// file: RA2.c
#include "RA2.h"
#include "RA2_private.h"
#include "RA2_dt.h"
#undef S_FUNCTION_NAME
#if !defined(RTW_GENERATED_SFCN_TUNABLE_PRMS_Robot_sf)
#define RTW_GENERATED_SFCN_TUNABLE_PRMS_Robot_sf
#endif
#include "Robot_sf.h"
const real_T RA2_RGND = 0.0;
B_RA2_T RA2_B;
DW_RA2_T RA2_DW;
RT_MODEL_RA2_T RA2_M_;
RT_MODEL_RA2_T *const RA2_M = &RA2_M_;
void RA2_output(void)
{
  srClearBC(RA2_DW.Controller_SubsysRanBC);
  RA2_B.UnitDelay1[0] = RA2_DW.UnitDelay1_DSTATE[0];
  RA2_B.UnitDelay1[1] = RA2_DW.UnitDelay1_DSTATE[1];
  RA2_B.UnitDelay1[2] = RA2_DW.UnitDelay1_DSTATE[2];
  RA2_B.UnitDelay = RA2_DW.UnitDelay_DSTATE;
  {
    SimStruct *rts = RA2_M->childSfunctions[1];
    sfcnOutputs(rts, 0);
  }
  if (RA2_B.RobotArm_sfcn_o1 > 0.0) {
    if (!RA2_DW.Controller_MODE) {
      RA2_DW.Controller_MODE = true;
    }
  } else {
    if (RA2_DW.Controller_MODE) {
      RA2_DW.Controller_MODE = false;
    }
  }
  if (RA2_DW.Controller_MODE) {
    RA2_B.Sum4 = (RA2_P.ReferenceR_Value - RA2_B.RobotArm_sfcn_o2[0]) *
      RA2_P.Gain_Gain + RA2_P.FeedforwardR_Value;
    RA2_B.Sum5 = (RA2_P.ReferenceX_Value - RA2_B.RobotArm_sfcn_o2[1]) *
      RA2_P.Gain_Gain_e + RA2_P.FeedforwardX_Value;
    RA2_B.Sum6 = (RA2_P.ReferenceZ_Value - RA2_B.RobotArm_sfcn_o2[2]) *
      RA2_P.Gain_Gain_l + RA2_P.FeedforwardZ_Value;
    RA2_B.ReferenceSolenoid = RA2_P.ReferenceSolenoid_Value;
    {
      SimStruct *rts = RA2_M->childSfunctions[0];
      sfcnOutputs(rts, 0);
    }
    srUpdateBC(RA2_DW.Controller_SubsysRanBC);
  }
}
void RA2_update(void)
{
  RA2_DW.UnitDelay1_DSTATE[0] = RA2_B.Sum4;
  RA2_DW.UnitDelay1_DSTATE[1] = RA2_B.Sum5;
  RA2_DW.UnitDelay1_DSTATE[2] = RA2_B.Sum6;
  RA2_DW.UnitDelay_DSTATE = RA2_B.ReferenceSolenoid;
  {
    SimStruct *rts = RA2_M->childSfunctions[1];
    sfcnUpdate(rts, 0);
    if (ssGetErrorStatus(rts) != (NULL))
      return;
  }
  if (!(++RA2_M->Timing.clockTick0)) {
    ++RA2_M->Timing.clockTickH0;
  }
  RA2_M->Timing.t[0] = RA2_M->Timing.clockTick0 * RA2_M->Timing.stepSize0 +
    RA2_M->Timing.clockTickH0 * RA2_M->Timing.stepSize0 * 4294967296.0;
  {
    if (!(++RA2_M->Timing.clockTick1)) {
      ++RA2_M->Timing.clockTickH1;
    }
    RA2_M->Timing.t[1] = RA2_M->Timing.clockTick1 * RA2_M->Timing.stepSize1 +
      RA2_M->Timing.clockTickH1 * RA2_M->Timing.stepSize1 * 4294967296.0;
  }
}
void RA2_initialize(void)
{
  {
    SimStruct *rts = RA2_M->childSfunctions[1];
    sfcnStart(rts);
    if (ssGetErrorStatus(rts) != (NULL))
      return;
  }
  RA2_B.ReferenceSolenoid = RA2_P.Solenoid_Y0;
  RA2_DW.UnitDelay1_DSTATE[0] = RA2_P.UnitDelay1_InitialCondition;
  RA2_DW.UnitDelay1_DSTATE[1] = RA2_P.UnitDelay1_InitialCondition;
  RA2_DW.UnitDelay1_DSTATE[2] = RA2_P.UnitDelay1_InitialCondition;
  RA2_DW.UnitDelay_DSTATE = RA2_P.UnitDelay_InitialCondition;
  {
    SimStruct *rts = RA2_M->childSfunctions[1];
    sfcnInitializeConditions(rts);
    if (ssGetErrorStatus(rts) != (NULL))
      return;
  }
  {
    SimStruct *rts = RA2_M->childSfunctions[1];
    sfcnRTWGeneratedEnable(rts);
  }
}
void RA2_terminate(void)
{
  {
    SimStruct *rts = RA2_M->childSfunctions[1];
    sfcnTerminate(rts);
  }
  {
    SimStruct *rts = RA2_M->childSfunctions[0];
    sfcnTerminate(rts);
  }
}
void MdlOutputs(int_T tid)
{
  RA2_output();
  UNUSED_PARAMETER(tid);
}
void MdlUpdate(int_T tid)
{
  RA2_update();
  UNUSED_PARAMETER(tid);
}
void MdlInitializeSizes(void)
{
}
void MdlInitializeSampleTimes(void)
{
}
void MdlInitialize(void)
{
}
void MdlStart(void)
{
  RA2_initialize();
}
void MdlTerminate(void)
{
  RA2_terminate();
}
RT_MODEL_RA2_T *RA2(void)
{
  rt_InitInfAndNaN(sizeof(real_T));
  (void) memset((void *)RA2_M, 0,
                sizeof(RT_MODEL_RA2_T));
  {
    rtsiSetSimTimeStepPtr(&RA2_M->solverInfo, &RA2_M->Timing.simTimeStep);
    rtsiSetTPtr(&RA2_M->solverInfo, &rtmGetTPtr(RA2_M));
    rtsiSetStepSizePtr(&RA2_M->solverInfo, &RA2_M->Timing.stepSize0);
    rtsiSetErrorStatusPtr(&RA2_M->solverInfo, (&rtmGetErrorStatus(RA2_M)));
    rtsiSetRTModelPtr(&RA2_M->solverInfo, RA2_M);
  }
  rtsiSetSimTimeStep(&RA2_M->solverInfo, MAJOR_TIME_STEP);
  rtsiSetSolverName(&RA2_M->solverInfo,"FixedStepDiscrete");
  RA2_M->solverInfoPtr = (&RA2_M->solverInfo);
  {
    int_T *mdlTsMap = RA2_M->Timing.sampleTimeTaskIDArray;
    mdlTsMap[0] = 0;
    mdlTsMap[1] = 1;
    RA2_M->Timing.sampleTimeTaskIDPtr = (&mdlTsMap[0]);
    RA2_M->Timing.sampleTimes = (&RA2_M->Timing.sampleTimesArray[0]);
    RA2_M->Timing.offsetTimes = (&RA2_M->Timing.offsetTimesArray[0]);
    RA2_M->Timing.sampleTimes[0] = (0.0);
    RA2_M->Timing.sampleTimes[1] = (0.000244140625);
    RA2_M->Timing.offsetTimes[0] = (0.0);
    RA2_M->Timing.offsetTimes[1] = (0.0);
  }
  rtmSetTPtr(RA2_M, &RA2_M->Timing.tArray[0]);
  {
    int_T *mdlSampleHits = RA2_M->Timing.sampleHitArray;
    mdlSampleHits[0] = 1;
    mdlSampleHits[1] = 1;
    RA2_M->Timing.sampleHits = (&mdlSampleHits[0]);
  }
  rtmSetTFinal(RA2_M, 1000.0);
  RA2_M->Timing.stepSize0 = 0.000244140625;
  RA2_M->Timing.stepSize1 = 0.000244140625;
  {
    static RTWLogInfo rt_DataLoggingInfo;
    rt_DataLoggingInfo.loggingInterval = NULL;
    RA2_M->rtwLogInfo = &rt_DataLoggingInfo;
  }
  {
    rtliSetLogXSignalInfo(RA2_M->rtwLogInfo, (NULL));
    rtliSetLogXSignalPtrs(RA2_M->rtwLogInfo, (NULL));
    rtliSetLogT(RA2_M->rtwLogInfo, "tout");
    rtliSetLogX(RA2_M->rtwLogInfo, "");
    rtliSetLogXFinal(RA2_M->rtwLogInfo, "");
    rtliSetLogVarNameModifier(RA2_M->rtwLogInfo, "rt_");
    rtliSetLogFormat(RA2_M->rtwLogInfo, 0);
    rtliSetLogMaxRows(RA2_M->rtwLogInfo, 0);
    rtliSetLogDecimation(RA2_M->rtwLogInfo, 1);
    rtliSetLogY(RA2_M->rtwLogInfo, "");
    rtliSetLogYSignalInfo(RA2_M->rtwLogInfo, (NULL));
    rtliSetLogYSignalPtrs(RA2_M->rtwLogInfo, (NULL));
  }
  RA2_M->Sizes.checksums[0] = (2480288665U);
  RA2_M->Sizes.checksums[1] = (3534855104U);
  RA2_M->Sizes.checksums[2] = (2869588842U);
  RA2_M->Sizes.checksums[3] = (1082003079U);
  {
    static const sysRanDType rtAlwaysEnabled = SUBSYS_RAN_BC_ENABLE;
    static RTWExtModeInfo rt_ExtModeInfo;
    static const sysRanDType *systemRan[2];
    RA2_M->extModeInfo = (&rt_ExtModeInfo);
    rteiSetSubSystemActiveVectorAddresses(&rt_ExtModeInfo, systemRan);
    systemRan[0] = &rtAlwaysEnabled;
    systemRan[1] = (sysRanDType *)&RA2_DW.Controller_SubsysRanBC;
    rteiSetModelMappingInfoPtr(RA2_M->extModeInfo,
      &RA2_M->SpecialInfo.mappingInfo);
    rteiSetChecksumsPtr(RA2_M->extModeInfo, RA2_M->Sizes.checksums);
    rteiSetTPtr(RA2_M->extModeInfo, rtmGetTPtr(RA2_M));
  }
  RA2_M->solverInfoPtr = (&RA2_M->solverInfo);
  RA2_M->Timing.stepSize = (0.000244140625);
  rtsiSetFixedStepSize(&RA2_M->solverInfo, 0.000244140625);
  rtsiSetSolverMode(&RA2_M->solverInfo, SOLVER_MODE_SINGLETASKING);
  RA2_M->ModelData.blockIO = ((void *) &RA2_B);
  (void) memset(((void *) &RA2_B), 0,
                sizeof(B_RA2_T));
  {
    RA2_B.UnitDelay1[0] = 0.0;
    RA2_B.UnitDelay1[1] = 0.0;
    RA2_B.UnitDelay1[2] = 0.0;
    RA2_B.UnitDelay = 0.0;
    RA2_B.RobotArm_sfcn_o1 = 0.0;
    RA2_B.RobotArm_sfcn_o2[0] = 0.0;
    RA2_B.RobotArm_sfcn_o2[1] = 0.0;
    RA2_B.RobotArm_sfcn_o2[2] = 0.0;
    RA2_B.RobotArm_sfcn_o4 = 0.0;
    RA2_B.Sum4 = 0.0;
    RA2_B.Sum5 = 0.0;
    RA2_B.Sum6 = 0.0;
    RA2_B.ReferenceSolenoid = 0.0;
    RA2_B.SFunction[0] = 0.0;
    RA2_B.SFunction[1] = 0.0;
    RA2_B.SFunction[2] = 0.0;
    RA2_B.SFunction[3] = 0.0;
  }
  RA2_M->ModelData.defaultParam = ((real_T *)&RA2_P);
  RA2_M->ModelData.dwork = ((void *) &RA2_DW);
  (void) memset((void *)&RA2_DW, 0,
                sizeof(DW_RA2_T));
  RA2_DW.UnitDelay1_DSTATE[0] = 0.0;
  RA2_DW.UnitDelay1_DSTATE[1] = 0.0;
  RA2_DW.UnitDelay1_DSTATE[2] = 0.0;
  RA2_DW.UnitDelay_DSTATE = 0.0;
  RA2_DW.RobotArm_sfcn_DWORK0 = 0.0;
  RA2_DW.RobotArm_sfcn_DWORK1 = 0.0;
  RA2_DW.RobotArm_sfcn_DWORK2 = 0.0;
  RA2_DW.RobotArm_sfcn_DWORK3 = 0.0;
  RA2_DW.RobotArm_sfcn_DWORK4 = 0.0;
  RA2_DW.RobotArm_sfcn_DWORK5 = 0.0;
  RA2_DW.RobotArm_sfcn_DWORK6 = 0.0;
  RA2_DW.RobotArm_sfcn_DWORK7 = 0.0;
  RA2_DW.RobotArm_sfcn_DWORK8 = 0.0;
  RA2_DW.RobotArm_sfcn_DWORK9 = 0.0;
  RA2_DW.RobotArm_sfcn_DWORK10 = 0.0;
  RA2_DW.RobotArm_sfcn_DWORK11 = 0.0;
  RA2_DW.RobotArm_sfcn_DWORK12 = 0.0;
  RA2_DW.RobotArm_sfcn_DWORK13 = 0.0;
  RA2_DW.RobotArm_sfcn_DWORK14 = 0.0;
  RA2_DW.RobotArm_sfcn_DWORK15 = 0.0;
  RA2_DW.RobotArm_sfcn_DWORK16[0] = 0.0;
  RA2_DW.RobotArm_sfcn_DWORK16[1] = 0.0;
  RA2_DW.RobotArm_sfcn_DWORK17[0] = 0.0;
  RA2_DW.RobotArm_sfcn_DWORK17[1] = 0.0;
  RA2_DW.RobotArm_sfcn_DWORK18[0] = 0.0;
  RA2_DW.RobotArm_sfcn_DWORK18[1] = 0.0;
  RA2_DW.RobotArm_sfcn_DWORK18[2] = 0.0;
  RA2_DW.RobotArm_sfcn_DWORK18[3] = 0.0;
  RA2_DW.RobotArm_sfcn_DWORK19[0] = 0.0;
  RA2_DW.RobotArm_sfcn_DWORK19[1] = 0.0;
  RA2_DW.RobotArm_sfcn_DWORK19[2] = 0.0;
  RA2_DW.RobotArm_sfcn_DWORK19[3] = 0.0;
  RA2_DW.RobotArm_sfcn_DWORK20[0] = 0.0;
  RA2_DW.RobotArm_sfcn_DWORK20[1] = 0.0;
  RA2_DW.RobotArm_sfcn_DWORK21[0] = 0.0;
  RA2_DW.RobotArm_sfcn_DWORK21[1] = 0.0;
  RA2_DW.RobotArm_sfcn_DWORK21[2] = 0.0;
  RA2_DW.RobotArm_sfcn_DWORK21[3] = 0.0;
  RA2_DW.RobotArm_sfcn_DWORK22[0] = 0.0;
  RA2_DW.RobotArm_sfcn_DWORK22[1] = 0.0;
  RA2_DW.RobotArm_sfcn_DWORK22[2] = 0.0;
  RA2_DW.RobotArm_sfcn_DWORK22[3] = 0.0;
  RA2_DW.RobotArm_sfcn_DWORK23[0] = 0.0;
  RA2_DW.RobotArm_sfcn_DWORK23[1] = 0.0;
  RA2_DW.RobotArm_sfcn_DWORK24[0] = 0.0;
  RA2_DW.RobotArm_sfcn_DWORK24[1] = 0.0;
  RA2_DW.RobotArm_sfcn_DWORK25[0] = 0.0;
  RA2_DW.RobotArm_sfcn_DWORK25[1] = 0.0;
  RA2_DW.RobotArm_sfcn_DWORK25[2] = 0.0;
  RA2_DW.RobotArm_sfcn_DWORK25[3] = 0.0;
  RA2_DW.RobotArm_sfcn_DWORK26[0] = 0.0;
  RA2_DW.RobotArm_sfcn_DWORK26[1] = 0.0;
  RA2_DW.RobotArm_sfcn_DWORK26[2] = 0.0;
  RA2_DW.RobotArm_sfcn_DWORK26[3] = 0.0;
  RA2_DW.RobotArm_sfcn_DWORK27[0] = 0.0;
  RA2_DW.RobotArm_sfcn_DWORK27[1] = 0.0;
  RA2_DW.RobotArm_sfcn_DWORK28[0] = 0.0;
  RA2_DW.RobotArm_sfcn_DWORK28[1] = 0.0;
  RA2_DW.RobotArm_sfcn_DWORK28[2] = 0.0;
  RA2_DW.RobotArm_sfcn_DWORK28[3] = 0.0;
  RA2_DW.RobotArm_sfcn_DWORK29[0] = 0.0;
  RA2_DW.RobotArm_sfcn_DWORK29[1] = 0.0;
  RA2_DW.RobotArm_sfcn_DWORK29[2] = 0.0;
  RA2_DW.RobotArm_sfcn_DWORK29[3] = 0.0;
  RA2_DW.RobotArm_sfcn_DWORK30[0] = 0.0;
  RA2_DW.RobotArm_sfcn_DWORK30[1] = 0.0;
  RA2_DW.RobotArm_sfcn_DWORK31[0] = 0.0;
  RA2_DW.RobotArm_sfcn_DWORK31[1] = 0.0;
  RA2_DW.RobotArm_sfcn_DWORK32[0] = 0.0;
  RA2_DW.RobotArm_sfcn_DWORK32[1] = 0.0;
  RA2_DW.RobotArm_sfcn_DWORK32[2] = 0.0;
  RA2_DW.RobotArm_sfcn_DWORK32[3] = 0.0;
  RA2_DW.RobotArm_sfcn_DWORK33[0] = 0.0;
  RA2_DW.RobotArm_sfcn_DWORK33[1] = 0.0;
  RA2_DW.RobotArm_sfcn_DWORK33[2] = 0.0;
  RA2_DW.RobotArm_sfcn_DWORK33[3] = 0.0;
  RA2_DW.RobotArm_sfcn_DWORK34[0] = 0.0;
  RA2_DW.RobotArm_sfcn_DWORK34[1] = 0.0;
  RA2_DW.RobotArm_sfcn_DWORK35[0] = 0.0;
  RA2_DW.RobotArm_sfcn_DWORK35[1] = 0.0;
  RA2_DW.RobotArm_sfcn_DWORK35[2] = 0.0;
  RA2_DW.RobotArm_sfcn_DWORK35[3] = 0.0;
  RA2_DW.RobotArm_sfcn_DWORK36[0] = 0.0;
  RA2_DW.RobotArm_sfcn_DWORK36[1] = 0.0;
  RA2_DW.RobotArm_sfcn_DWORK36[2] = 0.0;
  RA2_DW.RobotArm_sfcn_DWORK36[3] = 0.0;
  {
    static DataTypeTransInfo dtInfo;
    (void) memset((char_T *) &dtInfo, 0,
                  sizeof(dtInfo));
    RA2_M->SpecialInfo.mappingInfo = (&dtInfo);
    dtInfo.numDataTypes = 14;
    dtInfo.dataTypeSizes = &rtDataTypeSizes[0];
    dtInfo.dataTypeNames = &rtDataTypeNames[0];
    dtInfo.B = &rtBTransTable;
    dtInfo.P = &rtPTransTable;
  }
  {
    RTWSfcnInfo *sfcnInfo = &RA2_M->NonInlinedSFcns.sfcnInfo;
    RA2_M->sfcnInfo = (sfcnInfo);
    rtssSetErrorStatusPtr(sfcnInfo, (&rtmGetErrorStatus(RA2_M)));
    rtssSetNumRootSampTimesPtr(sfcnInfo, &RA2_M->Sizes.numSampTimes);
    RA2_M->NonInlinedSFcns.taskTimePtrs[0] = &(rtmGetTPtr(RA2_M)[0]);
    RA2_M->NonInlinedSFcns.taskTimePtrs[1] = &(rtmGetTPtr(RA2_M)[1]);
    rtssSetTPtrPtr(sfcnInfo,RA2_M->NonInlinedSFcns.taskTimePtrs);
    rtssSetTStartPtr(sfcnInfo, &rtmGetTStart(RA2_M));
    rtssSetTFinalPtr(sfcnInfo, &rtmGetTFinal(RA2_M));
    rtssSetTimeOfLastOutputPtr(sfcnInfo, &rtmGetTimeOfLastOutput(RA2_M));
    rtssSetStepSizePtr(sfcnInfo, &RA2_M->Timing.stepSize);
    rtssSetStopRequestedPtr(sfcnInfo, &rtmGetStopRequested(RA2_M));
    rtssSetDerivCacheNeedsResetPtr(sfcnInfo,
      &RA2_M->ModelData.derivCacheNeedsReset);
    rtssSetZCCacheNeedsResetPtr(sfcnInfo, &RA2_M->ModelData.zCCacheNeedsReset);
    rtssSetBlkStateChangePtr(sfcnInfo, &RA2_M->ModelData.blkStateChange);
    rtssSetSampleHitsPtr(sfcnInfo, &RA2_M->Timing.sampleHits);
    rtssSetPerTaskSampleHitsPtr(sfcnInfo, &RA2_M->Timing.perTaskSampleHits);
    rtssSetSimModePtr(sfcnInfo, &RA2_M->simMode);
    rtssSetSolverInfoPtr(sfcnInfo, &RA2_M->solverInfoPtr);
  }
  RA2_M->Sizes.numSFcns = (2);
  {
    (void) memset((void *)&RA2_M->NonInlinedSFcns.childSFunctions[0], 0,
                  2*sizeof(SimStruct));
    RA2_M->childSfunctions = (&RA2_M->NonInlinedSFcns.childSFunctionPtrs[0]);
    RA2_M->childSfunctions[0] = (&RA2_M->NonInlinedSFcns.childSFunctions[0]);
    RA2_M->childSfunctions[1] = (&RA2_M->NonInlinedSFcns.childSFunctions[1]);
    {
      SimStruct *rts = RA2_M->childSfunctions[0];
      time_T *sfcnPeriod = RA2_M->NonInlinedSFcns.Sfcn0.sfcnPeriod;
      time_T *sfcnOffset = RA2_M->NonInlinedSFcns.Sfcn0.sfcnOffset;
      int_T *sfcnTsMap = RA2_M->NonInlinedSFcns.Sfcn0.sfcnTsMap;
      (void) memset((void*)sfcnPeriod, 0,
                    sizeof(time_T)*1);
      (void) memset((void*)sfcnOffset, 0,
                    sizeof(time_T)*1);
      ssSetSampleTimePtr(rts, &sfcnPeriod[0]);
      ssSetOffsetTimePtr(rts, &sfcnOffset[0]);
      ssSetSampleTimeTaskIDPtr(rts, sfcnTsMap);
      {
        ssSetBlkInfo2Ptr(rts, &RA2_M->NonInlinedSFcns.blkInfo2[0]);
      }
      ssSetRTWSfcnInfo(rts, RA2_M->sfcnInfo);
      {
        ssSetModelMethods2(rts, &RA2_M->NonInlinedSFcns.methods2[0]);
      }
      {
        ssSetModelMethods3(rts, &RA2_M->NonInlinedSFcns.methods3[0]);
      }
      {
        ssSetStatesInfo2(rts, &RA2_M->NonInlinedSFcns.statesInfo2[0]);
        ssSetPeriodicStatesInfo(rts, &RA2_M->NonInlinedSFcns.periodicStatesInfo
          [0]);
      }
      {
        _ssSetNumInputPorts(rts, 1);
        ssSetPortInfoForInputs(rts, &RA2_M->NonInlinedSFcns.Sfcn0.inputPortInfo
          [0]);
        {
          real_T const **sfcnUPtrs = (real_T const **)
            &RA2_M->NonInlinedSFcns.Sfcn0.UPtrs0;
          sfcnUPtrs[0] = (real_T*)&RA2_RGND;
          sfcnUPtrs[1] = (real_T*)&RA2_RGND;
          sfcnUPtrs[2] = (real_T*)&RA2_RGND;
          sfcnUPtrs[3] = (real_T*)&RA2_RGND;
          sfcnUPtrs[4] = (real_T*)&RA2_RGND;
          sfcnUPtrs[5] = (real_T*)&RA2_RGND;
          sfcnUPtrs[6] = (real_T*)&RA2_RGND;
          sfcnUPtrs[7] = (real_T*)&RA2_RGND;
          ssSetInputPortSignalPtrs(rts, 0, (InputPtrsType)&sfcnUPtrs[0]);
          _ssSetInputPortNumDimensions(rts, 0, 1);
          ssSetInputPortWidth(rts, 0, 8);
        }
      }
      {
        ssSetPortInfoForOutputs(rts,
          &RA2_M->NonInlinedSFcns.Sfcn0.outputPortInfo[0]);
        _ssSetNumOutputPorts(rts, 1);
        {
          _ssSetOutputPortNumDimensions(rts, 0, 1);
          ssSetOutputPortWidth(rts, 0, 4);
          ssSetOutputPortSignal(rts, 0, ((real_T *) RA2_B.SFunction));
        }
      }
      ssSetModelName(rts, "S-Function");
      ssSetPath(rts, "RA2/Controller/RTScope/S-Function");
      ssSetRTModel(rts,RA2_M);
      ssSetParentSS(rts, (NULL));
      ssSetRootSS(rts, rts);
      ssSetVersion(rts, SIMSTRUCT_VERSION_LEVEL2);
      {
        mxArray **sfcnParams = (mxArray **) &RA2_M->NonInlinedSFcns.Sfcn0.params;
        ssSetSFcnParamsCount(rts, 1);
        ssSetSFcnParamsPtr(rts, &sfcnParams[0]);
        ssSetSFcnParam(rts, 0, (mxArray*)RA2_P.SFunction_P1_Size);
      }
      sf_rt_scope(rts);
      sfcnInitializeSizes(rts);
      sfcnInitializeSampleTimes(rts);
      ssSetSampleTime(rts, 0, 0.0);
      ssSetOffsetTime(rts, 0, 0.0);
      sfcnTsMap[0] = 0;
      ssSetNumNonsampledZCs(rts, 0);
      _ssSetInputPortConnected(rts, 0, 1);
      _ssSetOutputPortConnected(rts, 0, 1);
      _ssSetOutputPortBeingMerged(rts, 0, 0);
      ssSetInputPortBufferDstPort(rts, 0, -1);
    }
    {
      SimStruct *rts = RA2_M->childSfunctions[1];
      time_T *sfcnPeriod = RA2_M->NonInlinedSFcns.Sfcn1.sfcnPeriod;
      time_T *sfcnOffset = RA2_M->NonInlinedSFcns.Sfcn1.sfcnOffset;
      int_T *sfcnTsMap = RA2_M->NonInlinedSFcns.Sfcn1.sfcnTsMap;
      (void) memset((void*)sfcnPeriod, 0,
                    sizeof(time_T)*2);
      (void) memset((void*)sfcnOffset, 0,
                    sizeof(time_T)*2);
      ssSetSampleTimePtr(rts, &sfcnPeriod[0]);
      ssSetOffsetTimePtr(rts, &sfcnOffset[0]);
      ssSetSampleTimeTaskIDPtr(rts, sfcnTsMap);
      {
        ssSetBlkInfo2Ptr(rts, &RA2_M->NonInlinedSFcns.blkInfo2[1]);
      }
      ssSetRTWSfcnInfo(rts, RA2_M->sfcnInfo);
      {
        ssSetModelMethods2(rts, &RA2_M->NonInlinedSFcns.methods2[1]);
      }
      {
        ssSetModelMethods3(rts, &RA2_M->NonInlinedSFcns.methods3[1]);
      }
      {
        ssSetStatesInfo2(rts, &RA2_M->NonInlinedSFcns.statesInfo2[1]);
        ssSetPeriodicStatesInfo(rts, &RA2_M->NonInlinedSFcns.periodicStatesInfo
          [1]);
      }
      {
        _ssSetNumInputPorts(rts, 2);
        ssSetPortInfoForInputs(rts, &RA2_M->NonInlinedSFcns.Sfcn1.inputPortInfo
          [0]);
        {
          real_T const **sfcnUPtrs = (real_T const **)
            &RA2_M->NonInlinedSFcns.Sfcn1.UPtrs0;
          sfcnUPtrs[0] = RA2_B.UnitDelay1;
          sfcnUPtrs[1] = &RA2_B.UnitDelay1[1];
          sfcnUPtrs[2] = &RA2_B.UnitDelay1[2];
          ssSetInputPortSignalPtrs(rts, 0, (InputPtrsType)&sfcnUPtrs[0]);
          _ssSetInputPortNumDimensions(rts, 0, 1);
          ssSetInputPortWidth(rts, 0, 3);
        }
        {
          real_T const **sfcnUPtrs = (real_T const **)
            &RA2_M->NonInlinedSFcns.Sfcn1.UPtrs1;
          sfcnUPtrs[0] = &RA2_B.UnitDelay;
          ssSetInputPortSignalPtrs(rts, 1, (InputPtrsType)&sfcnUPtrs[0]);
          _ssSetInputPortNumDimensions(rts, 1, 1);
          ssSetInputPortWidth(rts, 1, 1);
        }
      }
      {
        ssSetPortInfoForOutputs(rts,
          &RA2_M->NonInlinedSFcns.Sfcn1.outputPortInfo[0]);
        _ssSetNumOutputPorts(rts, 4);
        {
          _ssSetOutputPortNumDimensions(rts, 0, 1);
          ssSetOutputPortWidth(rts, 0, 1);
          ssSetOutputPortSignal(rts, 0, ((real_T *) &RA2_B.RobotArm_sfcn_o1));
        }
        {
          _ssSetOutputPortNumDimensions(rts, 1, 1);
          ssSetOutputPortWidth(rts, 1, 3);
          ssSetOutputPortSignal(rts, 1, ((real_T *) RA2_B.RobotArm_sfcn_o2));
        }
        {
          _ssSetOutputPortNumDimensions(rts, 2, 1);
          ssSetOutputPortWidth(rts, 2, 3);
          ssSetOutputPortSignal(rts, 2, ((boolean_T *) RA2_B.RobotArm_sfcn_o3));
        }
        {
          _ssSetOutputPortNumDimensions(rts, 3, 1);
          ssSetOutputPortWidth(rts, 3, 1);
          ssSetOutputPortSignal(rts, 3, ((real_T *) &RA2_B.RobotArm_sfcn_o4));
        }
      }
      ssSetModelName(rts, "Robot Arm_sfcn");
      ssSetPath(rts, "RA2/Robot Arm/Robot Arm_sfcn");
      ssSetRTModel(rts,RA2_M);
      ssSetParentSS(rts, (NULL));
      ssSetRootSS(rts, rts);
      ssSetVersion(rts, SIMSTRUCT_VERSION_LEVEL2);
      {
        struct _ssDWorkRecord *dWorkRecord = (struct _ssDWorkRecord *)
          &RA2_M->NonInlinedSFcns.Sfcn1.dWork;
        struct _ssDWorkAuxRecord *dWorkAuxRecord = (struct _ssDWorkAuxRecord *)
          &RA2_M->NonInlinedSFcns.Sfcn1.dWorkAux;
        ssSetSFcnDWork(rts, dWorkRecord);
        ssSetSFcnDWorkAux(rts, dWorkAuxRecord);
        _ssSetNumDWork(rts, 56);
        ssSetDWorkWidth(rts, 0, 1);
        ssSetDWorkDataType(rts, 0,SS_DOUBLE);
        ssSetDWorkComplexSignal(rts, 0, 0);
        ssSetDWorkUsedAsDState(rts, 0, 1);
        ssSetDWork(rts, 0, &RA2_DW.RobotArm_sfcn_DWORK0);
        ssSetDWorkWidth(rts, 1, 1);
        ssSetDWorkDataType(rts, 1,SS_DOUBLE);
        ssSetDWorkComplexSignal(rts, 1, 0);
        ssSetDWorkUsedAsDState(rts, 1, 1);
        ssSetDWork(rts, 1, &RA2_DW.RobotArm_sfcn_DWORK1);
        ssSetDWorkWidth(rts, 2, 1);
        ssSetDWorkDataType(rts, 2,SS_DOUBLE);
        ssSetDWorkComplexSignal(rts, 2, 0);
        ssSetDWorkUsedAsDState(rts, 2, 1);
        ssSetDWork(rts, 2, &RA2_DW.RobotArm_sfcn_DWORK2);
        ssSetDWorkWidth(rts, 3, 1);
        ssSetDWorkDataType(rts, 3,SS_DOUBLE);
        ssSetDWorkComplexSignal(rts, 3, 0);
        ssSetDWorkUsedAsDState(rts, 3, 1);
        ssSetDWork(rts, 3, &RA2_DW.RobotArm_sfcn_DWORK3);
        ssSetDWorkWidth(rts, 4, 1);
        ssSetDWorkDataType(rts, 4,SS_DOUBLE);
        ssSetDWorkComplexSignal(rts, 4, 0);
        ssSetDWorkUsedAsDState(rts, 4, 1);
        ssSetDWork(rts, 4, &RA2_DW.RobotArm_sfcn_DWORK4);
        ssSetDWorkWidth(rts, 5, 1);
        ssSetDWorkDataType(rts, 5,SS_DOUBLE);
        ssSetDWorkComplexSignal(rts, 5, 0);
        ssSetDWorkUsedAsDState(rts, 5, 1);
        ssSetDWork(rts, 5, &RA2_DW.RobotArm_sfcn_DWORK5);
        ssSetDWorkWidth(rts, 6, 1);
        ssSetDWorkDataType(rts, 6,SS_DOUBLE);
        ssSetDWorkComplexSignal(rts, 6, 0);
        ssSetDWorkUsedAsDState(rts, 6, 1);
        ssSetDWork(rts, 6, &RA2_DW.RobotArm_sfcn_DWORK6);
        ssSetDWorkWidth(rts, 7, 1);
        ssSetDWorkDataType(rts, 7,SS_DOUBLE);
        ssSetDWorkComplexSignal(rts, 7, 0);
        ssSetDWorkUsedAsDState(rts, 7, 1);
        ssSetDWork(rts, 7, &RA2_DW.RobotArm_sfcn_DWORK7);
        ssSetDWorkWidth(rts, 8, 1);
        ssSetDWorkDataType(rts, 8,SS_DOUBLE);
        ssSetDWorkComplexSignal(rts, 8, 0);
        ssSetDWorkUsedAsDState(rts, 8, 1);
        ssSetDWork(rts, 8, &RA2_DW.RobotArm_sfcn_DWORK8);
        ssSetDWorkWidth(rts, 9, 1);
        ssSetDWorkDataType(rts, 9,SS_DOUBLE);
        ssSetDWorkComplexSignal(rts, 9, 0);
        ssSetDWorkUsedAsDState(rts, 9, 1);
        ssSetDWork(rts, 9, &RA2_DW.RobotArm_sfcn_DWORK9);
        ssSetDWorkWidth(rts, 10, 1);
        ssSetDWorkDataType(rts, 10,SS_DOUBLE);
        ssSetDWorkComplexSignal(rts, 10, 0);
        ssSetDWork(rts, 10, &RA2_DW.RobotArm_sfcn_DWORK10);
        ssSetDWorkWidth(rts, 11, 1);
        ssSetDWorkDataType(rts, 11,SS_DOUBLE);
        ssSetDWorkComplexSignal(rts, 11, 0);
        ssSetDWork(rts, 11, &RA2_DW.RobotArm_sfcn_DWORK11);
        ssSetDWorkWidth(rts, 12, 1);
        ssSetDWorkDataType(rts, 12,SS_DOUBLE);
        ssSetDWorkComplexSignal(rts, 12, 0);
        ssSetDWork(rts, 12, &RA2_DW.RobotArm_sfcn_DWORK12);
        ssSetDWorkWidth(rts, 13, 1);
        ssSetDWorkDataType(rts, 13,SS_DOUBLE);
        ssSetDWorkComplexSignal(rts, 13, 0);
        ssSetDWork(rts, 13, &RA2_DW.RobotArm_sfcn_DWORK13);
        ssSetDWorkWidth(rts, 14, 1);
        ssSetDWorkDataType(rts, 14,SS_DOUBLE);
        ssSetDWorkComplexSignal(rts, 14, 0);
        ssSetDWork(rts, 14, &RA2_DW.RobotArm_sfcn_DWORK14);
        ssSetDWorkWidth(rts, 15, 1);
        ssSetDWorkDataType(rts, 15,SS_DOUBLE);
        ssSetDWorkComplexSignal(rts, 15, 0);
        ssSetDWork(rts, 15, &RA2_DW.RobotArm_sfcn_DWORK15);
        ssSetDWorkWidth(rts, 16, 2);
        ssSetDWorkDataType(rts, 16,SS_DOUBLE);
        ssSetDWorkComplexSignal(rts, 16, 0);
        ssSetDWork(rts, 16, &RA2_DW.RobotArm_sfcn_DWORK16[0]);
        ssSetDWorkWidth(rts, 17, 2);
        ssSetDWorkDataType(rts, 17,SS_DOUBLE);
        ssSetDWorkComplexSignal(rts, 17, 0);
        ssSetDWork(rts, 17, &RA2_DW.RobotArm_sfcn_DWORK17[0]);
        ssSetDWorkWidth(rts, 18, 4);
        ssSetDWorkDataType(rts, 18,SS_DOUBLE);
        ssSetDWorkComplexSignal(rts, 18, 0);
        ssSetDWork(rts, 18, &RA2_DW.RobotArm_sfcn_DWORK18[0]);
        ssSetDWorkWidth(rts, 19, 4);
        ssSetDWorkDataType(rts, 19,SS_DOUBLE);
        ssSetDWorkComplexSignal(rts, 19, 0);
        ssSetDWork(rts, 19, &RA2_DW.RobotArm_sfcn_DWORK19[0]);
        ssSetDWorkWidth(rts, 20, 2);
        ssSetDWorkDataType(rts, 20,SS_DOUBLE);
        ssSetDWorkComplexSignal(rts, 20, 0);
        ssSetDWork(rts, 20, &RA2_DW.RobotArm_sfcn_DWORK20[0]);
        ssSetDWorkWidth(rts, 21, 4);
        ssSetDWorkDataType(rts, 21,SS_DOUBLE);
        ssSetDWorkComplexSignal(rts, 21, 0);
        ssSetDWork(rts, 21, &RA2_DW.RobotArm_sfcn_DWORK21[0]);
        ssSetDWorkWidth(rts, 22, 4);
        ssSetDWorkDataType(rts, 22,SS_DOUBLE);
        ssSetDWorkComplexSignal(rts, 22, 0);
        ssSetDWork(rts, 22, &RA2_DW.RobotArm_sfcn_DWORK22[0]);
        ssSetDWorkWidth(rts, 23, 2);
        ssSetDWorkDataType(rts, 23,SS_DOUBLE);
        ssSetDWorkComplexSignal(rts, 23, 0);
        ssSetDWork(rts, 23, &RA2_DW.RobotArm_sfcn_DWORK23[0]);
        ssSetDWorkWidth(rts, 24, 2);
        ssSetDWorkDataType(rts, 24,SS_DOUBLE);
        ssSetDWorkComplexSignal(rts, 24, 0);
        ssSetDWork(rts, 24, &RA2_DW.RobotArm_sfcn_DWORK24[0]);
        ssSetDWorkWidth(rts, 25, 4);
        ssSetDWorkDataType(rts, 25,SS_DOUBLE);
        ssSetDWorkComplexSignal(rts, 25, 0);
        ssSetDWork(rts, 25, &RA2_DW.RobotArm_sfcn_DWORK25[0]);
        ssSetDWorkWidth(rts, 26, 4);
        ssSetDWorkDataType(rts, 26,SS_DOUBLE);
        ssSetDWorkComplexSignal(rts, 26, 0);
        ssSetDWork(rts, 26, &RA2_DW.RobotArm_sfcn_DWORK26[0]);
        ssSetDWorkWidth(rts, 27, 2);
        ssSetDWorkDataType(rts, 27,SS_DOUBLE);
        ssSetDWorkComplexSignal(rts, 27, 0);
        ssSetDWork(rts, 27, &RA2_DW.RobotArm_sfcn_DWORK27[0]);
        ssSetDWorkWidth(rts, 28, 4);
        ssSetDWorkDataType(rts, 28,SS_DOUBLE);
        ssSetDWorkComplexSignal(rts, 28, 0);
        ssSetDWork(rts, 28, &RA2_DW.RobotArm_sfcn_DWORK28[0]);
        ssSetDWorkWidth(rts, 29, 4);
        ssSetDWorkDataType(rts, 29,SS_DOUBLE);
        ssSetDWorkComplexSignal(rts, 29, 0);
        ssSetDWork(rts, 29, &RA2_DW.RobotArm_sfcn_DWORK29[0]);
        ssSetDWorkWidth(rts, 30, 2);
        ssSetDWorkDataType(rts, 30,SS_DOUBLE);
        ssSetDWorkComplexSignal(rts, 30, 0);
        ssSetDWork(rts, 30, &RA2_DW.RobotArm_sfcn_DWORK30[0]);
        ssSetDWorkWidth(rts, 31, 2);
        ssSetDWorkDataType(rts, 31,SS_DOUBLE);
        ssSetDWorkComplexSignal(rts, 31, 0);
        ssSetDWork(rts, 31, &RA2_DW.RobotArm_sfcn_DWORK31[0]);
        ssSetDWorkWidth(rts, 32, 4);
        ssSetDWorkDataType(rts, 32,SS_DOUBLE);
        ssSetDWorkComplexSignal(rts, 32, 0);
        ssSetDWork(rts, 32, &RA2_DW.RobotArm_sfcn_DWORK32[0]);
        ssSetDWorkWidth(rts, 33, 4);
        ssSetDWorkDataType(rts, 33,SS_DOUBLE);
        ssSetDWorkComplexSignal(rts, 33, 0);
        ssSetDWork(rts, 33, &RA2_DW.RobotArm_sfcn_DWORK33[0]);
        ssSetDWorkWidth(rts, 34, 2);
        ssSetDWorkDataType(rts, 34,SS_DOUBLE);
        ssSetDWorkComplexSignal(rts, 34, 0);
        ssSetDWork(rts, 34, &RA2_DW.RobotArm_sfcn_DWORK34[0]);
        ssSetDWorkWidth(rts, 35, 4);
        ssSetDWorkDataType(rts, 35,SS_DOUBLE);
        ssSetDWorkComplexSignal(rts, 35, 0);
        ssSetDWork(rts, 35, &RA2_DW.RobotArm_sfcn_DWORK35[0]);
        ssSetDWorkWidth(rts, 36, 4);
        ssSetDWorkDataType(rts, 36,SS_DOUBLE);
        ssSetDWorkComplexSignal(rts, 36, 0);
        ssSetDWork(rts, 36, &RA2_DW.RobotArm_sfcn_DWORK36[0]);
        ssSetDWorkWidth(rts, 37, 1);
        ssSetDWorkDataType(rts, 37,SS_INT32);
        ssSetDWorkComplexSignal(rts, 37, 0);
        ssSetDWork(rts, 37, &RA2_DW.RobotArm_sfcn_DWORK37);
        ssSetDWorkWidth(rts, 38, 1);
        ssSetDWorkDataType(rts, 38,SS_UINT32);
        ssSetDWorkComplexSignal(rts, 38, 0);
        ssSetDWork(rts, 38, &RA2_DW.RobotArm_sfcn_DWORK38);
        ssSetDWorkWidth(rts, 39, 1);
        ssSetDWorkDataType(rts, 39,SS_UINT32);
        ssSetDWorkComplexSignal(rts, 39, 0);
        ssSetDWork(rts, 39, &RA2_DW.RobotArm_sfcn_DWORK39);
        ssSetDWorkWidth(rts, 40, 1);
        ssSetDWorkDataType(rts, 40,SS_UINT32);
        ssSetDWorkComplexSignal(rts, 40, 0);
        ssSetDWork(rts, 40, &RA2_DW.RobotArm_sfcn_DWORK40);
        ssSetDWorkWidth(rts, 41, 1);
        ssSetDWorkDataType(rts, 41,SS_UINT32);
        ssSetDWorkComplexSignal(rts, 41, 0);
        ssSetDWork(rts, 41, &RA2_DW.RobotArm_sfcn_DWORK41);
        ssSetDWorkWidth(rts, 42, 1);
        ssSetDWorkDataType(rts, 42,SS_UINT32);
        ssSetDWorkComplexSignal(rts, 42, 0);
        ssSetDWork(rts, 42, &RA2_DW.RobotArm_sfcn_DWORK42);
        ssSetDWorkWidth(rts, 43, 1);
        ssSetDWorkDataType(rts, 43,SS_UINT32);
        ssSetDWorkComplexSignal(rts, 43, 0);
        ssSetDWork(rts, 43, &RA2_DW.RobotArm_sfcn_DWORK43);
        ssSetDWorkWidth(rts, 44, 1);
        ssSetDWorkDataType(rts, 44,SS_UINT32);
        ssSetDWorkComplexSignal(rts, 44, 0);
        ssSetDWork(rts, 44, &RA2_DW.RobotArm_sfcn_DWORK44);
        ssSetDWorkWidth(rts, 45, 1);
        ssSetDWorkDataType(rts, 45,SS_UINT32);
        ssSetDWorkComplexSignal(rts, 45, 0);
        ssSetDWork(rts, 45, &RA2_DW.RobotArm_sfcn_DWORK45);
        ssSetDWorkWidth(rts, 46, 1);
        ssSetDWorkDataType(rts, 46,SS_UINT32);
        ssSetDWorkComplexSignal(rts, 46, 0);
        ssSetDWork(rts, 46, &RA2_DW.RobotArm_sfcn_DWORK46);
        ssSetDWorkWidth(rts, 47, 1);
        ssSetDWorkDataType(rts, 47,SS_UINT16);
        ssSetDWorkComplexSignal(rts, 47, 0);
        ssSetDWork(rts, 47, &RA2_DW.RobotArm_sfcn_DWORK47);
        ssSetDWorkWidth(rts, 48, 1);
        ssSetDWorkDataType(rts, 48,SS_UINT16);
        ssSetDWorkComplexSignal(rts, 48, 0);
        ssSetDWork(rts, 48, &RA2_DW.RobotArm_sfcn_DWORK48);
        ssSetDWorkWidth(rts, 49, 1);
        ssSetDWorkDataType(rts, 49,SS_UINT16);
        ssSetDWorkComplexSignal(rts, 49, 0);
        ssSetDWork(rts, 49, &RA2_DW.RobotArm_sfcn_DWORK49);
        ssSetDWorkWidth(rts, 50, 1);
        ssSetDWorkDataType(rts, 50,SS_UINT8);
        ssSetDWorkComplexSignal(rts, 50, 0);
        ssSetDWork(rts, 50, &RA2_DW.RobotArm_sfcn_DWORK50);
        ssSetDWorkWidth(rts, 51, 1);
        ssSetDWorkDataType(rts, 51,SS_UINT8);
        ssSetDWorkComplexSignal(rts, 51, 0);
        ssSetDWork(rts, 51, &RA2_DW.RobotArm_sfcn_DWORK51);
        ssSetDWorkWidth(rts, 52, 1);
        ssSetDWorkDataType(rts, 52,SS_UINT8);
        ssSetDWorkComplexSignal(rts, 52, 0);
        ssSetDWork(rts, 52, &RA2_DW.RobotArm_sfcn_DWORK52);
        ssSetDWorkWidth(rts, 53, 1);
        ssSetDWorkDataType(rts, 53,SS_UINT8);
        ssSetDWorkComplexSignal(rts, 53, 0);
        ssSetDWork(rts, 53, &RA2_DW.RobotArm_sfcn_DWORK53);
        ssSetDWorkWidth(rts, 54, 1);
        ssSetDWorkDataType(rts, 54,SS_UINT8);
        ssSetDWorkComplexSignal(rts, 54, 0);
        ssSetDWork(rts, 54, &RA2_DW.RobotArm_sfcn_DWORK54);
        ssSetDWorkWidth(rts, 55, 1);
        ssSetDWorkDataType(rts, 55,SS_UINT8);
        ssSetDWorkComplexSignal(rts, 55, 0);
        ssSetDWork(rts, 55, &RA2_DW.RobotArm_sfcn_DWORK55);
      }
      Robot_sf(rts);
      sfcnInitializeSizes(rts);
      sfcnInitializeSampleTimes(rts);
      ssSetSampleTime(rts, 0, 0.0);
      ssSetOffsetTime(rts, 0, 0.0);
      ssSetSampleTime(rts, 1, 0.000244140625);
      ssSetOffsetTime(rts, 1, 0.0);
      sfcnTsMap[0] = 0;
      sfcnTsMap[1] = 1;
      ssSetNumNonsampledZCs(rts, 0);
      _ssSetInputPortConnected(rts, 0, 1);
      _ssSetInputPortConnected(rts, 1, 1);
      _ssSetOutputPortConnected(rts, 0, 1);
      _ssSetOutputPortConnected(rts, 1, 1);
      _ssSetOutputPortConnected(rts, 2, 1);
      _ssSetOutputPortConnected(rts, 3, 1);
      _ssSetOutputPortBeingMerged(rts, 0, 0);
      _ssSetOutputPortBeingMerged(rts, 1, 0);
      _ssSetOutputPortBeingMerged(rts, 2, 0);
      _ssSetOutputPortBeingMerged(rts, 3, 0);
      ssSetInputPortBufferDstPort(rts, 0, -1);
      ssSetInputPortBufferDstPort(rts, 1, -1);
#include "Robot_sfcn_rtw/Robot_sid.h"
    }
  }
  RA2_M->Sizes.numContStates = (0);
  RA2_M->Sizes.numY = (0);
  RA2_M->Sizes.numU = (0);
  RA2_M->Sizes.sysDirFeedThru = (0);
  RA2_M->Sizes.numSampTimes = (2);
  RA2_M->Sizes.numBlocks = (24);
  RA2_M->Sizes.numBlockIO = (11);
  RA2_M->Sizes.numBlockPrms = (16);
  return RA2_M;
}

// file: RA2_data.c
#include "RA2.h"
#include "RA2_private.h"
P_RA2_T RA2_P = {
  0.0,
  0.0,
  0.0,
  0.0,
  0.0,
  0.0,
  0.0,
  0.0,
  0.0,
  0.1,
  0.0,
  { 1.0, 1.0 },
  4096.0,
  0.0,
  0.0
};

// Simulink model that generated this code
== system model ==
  UnitDelay1 : UnitDelay  <- 1: Controller
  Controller : Subsystem  <- 1: RobotArm_sfcn/2, Enable: RobotArm_sfcn
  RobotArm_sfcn : S-Function  FunctionName=Robot_sf  <- 1: UnitDelay1, 2: UnitDelay
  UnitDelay : UnitDelay  <- 1: Controller/2
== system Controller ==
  Inport#1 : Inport
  EnablePort#1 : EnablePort
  Outport#1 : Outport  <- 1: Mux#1
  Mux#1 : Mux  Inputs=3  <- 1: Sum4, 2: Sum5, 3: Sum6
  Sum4 : Sum  Inputs=++  <- 1: FeedforwardR, 2: Gain
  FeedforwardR : Constant  Value=0
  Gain : Gain  Gain=0  <- 1: Sum#1
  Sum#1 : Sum  Inputs=+-  <- 1: ReferenceR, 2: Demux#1
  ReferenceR : Constant  Value=0
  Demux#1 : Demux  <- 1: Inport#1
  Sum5 : Sum  Inputs=++  <- 1: FeedforwardX, 2: Gain#1
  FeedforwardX : Constant  Value=0
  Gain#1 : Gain  Gain=0  <- 1: Sum#2
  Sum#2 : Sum  Inputs=+-  <- 1: ReferenceX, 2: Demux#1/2
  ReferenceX : Constant  Value=0
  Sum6 : Sum  Inputs=++  <- 1: FeedforwardZ, 2: Gain#2
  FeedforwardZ : Constant  Value=0.1
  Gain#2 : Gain  Gain=0  <- 1: Sum#3
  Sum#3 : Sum  Inputs=+-  <- 1: ReferenceZ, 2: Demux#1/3
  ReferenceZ : Constant  Value=0
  Solenoid : Outport  InitialOutput=0  <- 1: ReferenceSolenoid
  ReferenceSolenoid : Constant  Value=0
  SFunction : S-Function  FunctionName=sf_rt_scope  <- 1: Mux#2
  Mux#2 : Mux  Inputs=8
